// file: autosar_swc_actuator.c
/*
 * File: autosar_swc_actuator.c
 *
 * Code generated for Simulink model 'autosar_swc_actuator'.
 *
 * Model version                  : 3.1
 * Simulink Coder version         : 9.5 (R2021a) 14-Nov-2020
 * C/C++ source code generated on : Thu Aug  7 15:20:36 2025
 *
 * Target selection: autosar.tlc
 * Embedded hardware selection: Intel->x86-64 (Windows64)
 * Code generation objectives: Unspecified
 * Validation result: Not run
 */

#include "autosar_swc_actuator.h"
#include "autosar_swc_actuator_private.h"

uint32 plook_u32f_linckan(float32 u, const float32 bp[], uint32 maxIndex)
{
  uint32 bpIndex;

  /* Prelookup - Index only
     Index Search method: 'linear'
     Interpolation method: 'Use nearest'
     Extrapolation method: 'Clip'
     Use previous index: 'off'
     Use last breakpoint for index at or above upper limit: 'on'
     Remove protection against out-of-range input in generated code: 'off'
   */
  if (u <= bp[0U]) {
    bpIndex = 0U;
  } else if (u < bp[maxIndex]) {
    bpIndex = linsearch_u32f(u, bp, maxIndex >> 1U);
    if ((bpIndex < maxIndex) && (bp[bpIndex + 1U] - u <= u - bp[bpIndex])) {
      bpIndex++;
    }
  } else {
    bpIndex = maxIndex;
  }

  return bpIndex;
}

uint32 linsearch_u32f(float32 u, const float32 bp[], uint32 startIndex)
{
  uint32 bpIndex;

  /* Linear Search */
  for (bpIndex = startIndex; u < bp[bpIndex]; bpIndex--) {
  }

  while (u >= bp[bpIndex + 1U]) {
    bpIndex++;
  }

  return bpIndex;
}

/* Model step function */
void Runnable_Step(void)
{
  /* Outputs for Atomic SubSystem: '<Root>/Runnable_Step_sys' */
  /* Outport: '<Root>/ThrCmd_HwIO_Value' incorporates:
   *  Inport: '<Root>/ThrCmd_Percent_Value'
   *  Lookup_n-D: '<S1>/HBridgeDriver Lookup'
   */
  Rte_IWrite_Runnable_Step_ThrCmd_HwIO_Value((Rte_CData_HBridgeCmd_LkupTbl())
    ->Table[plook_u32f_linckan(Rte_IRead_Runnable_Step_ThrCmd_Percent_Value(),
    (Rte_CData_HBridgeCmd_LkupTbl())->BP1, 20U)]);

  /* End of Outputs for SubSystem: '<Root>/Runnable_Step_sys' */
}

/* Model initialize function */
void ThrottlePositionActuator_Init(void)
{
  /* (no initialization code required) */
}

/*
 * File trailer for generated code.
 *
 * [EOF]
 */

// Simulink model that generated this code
simulink model "autosar_swc_actuator"  (R2021a)
settings: Solver=FixedStepDiscrete  StartTime=0.0  StopTime=10.0  FixedStep=0.005  RelTol=1e-3
model workspace (MATLAB code in the model file):
  | HBridgeCmd_LkupTbl = Simulink.LookupTable;
  | HBridgeCmd_LkupTbl.Table.DataType = 'int16';
  | HBridgeCmd_LkupTbl.Table.FieldName = 'Table';
  | HBridgeCmd_LkupTbl.Table.Value = int16( ...
  |   [-2048 -1843 -1638 -1434 -1229 -1024 -819 -614 -410 -205 0 205 410 614 ...
  |    819 1024 1229 1434 1638 1843 2048]);
  | HBridgeCmd_LkupTbl.BreakpointsSpecification = 'Explicit values';
  | HBridgeCmd_LkupTbl.SupportTunableSize = false;
  | HBridgeCmd_LkupTbl.Breakpoints.DataType = 'single';
  | HBridgeCmd_LkupTbl.Breakpoints.FieldName = 'BP1';
  | HBridgeCmd_LkupTbl.Breakpoints.Value = ...
  |   [-100 -90 -80 -70 -60 -50 -40 -30 -20 -10 0 10 20 30 40 50 60 70 80 90 ...
  |    100];
  | HBridgeCmd_LkupTbl.Breakpoints.TunableSizeName = 'N1';
  | HBridgeCmd_LkupTbl.StructTypeInfo.Name = 'MyStruct_Actuator';
  | HBridgeCmd_LkupTbl.StructTypeInfo.HeaderFileName = 'Rte_Type.h';
undefined symbols (not defined in the file): TPSPercentBkpt, TPSPercentTbl

== system autosar_swc_actuator ==
  note: Copyright 2017-2019 The MathWorks, Inc.
  ThrCmd_Percent_Value : Inport  OutDataTypeStr=single  PortDimensions=1
  Runnable_Step_sys : Subsystem  TreatAsAtomicUnit=on  SystemSampleTime=0.005
  ThrCmd_HwIO_Value : Outport  OutDataTypeStr=int16  PortDimensions=1  VectorParamsAs1DForOutWhenUnconnected=off
  wires:
  ThrCmd_Percent_Value/1 -> Runnable_Step_sys/1(ThrCmd_Percent_Value_read)
  Runnable_Step_sys/1(ThrCmd_HwIO_Value_write) -> ThrCmd_HwIO_Value/1

== system autosar_swc_actuator/Runnable_Step_sys ==
  ThrCmd_Percent_Value_read : Inport
  Data Type Conversion : DataTypeConversion  OutDataTypeStr=single
  HBridgeDriver Lookup : Lookup_n-D  NumberOfTableDimensions=1  DataSpecification=Lookup table object  LookupTableObject=HBridgeCmd_LkupTbl  BreakpointsForDimension1=TPSPercentBkpt  BreakpointsForDimension1DataTypeStr=single  IndexSearchMethod=Linear search  Table=TPSPercentTbl  TableDataTypeStr=single  InterpMethod=Nearest  InternalRulePriority=Speed  OutDataTypeStr=Inherit: Inherit from 'Table data'  RndMeth=Simplest  InputSameDT=on
  Scope : Scope  NumInputPorts=2
  ThrCmd_HwIO_Value_write : Outport  VectorParamsAs1DForOutWhenUnconnected=off
  wires:
  ThrCmd_Percent_Value_read/1 -> Data Type Conversion/1
  HBridgeDriver Lookup/1 -> Scope/2, ThrCmd_HwIO_Value_write/1
  Data Type Conversion/1 -> Scope/1, HBridgeDriver Lookup/1
